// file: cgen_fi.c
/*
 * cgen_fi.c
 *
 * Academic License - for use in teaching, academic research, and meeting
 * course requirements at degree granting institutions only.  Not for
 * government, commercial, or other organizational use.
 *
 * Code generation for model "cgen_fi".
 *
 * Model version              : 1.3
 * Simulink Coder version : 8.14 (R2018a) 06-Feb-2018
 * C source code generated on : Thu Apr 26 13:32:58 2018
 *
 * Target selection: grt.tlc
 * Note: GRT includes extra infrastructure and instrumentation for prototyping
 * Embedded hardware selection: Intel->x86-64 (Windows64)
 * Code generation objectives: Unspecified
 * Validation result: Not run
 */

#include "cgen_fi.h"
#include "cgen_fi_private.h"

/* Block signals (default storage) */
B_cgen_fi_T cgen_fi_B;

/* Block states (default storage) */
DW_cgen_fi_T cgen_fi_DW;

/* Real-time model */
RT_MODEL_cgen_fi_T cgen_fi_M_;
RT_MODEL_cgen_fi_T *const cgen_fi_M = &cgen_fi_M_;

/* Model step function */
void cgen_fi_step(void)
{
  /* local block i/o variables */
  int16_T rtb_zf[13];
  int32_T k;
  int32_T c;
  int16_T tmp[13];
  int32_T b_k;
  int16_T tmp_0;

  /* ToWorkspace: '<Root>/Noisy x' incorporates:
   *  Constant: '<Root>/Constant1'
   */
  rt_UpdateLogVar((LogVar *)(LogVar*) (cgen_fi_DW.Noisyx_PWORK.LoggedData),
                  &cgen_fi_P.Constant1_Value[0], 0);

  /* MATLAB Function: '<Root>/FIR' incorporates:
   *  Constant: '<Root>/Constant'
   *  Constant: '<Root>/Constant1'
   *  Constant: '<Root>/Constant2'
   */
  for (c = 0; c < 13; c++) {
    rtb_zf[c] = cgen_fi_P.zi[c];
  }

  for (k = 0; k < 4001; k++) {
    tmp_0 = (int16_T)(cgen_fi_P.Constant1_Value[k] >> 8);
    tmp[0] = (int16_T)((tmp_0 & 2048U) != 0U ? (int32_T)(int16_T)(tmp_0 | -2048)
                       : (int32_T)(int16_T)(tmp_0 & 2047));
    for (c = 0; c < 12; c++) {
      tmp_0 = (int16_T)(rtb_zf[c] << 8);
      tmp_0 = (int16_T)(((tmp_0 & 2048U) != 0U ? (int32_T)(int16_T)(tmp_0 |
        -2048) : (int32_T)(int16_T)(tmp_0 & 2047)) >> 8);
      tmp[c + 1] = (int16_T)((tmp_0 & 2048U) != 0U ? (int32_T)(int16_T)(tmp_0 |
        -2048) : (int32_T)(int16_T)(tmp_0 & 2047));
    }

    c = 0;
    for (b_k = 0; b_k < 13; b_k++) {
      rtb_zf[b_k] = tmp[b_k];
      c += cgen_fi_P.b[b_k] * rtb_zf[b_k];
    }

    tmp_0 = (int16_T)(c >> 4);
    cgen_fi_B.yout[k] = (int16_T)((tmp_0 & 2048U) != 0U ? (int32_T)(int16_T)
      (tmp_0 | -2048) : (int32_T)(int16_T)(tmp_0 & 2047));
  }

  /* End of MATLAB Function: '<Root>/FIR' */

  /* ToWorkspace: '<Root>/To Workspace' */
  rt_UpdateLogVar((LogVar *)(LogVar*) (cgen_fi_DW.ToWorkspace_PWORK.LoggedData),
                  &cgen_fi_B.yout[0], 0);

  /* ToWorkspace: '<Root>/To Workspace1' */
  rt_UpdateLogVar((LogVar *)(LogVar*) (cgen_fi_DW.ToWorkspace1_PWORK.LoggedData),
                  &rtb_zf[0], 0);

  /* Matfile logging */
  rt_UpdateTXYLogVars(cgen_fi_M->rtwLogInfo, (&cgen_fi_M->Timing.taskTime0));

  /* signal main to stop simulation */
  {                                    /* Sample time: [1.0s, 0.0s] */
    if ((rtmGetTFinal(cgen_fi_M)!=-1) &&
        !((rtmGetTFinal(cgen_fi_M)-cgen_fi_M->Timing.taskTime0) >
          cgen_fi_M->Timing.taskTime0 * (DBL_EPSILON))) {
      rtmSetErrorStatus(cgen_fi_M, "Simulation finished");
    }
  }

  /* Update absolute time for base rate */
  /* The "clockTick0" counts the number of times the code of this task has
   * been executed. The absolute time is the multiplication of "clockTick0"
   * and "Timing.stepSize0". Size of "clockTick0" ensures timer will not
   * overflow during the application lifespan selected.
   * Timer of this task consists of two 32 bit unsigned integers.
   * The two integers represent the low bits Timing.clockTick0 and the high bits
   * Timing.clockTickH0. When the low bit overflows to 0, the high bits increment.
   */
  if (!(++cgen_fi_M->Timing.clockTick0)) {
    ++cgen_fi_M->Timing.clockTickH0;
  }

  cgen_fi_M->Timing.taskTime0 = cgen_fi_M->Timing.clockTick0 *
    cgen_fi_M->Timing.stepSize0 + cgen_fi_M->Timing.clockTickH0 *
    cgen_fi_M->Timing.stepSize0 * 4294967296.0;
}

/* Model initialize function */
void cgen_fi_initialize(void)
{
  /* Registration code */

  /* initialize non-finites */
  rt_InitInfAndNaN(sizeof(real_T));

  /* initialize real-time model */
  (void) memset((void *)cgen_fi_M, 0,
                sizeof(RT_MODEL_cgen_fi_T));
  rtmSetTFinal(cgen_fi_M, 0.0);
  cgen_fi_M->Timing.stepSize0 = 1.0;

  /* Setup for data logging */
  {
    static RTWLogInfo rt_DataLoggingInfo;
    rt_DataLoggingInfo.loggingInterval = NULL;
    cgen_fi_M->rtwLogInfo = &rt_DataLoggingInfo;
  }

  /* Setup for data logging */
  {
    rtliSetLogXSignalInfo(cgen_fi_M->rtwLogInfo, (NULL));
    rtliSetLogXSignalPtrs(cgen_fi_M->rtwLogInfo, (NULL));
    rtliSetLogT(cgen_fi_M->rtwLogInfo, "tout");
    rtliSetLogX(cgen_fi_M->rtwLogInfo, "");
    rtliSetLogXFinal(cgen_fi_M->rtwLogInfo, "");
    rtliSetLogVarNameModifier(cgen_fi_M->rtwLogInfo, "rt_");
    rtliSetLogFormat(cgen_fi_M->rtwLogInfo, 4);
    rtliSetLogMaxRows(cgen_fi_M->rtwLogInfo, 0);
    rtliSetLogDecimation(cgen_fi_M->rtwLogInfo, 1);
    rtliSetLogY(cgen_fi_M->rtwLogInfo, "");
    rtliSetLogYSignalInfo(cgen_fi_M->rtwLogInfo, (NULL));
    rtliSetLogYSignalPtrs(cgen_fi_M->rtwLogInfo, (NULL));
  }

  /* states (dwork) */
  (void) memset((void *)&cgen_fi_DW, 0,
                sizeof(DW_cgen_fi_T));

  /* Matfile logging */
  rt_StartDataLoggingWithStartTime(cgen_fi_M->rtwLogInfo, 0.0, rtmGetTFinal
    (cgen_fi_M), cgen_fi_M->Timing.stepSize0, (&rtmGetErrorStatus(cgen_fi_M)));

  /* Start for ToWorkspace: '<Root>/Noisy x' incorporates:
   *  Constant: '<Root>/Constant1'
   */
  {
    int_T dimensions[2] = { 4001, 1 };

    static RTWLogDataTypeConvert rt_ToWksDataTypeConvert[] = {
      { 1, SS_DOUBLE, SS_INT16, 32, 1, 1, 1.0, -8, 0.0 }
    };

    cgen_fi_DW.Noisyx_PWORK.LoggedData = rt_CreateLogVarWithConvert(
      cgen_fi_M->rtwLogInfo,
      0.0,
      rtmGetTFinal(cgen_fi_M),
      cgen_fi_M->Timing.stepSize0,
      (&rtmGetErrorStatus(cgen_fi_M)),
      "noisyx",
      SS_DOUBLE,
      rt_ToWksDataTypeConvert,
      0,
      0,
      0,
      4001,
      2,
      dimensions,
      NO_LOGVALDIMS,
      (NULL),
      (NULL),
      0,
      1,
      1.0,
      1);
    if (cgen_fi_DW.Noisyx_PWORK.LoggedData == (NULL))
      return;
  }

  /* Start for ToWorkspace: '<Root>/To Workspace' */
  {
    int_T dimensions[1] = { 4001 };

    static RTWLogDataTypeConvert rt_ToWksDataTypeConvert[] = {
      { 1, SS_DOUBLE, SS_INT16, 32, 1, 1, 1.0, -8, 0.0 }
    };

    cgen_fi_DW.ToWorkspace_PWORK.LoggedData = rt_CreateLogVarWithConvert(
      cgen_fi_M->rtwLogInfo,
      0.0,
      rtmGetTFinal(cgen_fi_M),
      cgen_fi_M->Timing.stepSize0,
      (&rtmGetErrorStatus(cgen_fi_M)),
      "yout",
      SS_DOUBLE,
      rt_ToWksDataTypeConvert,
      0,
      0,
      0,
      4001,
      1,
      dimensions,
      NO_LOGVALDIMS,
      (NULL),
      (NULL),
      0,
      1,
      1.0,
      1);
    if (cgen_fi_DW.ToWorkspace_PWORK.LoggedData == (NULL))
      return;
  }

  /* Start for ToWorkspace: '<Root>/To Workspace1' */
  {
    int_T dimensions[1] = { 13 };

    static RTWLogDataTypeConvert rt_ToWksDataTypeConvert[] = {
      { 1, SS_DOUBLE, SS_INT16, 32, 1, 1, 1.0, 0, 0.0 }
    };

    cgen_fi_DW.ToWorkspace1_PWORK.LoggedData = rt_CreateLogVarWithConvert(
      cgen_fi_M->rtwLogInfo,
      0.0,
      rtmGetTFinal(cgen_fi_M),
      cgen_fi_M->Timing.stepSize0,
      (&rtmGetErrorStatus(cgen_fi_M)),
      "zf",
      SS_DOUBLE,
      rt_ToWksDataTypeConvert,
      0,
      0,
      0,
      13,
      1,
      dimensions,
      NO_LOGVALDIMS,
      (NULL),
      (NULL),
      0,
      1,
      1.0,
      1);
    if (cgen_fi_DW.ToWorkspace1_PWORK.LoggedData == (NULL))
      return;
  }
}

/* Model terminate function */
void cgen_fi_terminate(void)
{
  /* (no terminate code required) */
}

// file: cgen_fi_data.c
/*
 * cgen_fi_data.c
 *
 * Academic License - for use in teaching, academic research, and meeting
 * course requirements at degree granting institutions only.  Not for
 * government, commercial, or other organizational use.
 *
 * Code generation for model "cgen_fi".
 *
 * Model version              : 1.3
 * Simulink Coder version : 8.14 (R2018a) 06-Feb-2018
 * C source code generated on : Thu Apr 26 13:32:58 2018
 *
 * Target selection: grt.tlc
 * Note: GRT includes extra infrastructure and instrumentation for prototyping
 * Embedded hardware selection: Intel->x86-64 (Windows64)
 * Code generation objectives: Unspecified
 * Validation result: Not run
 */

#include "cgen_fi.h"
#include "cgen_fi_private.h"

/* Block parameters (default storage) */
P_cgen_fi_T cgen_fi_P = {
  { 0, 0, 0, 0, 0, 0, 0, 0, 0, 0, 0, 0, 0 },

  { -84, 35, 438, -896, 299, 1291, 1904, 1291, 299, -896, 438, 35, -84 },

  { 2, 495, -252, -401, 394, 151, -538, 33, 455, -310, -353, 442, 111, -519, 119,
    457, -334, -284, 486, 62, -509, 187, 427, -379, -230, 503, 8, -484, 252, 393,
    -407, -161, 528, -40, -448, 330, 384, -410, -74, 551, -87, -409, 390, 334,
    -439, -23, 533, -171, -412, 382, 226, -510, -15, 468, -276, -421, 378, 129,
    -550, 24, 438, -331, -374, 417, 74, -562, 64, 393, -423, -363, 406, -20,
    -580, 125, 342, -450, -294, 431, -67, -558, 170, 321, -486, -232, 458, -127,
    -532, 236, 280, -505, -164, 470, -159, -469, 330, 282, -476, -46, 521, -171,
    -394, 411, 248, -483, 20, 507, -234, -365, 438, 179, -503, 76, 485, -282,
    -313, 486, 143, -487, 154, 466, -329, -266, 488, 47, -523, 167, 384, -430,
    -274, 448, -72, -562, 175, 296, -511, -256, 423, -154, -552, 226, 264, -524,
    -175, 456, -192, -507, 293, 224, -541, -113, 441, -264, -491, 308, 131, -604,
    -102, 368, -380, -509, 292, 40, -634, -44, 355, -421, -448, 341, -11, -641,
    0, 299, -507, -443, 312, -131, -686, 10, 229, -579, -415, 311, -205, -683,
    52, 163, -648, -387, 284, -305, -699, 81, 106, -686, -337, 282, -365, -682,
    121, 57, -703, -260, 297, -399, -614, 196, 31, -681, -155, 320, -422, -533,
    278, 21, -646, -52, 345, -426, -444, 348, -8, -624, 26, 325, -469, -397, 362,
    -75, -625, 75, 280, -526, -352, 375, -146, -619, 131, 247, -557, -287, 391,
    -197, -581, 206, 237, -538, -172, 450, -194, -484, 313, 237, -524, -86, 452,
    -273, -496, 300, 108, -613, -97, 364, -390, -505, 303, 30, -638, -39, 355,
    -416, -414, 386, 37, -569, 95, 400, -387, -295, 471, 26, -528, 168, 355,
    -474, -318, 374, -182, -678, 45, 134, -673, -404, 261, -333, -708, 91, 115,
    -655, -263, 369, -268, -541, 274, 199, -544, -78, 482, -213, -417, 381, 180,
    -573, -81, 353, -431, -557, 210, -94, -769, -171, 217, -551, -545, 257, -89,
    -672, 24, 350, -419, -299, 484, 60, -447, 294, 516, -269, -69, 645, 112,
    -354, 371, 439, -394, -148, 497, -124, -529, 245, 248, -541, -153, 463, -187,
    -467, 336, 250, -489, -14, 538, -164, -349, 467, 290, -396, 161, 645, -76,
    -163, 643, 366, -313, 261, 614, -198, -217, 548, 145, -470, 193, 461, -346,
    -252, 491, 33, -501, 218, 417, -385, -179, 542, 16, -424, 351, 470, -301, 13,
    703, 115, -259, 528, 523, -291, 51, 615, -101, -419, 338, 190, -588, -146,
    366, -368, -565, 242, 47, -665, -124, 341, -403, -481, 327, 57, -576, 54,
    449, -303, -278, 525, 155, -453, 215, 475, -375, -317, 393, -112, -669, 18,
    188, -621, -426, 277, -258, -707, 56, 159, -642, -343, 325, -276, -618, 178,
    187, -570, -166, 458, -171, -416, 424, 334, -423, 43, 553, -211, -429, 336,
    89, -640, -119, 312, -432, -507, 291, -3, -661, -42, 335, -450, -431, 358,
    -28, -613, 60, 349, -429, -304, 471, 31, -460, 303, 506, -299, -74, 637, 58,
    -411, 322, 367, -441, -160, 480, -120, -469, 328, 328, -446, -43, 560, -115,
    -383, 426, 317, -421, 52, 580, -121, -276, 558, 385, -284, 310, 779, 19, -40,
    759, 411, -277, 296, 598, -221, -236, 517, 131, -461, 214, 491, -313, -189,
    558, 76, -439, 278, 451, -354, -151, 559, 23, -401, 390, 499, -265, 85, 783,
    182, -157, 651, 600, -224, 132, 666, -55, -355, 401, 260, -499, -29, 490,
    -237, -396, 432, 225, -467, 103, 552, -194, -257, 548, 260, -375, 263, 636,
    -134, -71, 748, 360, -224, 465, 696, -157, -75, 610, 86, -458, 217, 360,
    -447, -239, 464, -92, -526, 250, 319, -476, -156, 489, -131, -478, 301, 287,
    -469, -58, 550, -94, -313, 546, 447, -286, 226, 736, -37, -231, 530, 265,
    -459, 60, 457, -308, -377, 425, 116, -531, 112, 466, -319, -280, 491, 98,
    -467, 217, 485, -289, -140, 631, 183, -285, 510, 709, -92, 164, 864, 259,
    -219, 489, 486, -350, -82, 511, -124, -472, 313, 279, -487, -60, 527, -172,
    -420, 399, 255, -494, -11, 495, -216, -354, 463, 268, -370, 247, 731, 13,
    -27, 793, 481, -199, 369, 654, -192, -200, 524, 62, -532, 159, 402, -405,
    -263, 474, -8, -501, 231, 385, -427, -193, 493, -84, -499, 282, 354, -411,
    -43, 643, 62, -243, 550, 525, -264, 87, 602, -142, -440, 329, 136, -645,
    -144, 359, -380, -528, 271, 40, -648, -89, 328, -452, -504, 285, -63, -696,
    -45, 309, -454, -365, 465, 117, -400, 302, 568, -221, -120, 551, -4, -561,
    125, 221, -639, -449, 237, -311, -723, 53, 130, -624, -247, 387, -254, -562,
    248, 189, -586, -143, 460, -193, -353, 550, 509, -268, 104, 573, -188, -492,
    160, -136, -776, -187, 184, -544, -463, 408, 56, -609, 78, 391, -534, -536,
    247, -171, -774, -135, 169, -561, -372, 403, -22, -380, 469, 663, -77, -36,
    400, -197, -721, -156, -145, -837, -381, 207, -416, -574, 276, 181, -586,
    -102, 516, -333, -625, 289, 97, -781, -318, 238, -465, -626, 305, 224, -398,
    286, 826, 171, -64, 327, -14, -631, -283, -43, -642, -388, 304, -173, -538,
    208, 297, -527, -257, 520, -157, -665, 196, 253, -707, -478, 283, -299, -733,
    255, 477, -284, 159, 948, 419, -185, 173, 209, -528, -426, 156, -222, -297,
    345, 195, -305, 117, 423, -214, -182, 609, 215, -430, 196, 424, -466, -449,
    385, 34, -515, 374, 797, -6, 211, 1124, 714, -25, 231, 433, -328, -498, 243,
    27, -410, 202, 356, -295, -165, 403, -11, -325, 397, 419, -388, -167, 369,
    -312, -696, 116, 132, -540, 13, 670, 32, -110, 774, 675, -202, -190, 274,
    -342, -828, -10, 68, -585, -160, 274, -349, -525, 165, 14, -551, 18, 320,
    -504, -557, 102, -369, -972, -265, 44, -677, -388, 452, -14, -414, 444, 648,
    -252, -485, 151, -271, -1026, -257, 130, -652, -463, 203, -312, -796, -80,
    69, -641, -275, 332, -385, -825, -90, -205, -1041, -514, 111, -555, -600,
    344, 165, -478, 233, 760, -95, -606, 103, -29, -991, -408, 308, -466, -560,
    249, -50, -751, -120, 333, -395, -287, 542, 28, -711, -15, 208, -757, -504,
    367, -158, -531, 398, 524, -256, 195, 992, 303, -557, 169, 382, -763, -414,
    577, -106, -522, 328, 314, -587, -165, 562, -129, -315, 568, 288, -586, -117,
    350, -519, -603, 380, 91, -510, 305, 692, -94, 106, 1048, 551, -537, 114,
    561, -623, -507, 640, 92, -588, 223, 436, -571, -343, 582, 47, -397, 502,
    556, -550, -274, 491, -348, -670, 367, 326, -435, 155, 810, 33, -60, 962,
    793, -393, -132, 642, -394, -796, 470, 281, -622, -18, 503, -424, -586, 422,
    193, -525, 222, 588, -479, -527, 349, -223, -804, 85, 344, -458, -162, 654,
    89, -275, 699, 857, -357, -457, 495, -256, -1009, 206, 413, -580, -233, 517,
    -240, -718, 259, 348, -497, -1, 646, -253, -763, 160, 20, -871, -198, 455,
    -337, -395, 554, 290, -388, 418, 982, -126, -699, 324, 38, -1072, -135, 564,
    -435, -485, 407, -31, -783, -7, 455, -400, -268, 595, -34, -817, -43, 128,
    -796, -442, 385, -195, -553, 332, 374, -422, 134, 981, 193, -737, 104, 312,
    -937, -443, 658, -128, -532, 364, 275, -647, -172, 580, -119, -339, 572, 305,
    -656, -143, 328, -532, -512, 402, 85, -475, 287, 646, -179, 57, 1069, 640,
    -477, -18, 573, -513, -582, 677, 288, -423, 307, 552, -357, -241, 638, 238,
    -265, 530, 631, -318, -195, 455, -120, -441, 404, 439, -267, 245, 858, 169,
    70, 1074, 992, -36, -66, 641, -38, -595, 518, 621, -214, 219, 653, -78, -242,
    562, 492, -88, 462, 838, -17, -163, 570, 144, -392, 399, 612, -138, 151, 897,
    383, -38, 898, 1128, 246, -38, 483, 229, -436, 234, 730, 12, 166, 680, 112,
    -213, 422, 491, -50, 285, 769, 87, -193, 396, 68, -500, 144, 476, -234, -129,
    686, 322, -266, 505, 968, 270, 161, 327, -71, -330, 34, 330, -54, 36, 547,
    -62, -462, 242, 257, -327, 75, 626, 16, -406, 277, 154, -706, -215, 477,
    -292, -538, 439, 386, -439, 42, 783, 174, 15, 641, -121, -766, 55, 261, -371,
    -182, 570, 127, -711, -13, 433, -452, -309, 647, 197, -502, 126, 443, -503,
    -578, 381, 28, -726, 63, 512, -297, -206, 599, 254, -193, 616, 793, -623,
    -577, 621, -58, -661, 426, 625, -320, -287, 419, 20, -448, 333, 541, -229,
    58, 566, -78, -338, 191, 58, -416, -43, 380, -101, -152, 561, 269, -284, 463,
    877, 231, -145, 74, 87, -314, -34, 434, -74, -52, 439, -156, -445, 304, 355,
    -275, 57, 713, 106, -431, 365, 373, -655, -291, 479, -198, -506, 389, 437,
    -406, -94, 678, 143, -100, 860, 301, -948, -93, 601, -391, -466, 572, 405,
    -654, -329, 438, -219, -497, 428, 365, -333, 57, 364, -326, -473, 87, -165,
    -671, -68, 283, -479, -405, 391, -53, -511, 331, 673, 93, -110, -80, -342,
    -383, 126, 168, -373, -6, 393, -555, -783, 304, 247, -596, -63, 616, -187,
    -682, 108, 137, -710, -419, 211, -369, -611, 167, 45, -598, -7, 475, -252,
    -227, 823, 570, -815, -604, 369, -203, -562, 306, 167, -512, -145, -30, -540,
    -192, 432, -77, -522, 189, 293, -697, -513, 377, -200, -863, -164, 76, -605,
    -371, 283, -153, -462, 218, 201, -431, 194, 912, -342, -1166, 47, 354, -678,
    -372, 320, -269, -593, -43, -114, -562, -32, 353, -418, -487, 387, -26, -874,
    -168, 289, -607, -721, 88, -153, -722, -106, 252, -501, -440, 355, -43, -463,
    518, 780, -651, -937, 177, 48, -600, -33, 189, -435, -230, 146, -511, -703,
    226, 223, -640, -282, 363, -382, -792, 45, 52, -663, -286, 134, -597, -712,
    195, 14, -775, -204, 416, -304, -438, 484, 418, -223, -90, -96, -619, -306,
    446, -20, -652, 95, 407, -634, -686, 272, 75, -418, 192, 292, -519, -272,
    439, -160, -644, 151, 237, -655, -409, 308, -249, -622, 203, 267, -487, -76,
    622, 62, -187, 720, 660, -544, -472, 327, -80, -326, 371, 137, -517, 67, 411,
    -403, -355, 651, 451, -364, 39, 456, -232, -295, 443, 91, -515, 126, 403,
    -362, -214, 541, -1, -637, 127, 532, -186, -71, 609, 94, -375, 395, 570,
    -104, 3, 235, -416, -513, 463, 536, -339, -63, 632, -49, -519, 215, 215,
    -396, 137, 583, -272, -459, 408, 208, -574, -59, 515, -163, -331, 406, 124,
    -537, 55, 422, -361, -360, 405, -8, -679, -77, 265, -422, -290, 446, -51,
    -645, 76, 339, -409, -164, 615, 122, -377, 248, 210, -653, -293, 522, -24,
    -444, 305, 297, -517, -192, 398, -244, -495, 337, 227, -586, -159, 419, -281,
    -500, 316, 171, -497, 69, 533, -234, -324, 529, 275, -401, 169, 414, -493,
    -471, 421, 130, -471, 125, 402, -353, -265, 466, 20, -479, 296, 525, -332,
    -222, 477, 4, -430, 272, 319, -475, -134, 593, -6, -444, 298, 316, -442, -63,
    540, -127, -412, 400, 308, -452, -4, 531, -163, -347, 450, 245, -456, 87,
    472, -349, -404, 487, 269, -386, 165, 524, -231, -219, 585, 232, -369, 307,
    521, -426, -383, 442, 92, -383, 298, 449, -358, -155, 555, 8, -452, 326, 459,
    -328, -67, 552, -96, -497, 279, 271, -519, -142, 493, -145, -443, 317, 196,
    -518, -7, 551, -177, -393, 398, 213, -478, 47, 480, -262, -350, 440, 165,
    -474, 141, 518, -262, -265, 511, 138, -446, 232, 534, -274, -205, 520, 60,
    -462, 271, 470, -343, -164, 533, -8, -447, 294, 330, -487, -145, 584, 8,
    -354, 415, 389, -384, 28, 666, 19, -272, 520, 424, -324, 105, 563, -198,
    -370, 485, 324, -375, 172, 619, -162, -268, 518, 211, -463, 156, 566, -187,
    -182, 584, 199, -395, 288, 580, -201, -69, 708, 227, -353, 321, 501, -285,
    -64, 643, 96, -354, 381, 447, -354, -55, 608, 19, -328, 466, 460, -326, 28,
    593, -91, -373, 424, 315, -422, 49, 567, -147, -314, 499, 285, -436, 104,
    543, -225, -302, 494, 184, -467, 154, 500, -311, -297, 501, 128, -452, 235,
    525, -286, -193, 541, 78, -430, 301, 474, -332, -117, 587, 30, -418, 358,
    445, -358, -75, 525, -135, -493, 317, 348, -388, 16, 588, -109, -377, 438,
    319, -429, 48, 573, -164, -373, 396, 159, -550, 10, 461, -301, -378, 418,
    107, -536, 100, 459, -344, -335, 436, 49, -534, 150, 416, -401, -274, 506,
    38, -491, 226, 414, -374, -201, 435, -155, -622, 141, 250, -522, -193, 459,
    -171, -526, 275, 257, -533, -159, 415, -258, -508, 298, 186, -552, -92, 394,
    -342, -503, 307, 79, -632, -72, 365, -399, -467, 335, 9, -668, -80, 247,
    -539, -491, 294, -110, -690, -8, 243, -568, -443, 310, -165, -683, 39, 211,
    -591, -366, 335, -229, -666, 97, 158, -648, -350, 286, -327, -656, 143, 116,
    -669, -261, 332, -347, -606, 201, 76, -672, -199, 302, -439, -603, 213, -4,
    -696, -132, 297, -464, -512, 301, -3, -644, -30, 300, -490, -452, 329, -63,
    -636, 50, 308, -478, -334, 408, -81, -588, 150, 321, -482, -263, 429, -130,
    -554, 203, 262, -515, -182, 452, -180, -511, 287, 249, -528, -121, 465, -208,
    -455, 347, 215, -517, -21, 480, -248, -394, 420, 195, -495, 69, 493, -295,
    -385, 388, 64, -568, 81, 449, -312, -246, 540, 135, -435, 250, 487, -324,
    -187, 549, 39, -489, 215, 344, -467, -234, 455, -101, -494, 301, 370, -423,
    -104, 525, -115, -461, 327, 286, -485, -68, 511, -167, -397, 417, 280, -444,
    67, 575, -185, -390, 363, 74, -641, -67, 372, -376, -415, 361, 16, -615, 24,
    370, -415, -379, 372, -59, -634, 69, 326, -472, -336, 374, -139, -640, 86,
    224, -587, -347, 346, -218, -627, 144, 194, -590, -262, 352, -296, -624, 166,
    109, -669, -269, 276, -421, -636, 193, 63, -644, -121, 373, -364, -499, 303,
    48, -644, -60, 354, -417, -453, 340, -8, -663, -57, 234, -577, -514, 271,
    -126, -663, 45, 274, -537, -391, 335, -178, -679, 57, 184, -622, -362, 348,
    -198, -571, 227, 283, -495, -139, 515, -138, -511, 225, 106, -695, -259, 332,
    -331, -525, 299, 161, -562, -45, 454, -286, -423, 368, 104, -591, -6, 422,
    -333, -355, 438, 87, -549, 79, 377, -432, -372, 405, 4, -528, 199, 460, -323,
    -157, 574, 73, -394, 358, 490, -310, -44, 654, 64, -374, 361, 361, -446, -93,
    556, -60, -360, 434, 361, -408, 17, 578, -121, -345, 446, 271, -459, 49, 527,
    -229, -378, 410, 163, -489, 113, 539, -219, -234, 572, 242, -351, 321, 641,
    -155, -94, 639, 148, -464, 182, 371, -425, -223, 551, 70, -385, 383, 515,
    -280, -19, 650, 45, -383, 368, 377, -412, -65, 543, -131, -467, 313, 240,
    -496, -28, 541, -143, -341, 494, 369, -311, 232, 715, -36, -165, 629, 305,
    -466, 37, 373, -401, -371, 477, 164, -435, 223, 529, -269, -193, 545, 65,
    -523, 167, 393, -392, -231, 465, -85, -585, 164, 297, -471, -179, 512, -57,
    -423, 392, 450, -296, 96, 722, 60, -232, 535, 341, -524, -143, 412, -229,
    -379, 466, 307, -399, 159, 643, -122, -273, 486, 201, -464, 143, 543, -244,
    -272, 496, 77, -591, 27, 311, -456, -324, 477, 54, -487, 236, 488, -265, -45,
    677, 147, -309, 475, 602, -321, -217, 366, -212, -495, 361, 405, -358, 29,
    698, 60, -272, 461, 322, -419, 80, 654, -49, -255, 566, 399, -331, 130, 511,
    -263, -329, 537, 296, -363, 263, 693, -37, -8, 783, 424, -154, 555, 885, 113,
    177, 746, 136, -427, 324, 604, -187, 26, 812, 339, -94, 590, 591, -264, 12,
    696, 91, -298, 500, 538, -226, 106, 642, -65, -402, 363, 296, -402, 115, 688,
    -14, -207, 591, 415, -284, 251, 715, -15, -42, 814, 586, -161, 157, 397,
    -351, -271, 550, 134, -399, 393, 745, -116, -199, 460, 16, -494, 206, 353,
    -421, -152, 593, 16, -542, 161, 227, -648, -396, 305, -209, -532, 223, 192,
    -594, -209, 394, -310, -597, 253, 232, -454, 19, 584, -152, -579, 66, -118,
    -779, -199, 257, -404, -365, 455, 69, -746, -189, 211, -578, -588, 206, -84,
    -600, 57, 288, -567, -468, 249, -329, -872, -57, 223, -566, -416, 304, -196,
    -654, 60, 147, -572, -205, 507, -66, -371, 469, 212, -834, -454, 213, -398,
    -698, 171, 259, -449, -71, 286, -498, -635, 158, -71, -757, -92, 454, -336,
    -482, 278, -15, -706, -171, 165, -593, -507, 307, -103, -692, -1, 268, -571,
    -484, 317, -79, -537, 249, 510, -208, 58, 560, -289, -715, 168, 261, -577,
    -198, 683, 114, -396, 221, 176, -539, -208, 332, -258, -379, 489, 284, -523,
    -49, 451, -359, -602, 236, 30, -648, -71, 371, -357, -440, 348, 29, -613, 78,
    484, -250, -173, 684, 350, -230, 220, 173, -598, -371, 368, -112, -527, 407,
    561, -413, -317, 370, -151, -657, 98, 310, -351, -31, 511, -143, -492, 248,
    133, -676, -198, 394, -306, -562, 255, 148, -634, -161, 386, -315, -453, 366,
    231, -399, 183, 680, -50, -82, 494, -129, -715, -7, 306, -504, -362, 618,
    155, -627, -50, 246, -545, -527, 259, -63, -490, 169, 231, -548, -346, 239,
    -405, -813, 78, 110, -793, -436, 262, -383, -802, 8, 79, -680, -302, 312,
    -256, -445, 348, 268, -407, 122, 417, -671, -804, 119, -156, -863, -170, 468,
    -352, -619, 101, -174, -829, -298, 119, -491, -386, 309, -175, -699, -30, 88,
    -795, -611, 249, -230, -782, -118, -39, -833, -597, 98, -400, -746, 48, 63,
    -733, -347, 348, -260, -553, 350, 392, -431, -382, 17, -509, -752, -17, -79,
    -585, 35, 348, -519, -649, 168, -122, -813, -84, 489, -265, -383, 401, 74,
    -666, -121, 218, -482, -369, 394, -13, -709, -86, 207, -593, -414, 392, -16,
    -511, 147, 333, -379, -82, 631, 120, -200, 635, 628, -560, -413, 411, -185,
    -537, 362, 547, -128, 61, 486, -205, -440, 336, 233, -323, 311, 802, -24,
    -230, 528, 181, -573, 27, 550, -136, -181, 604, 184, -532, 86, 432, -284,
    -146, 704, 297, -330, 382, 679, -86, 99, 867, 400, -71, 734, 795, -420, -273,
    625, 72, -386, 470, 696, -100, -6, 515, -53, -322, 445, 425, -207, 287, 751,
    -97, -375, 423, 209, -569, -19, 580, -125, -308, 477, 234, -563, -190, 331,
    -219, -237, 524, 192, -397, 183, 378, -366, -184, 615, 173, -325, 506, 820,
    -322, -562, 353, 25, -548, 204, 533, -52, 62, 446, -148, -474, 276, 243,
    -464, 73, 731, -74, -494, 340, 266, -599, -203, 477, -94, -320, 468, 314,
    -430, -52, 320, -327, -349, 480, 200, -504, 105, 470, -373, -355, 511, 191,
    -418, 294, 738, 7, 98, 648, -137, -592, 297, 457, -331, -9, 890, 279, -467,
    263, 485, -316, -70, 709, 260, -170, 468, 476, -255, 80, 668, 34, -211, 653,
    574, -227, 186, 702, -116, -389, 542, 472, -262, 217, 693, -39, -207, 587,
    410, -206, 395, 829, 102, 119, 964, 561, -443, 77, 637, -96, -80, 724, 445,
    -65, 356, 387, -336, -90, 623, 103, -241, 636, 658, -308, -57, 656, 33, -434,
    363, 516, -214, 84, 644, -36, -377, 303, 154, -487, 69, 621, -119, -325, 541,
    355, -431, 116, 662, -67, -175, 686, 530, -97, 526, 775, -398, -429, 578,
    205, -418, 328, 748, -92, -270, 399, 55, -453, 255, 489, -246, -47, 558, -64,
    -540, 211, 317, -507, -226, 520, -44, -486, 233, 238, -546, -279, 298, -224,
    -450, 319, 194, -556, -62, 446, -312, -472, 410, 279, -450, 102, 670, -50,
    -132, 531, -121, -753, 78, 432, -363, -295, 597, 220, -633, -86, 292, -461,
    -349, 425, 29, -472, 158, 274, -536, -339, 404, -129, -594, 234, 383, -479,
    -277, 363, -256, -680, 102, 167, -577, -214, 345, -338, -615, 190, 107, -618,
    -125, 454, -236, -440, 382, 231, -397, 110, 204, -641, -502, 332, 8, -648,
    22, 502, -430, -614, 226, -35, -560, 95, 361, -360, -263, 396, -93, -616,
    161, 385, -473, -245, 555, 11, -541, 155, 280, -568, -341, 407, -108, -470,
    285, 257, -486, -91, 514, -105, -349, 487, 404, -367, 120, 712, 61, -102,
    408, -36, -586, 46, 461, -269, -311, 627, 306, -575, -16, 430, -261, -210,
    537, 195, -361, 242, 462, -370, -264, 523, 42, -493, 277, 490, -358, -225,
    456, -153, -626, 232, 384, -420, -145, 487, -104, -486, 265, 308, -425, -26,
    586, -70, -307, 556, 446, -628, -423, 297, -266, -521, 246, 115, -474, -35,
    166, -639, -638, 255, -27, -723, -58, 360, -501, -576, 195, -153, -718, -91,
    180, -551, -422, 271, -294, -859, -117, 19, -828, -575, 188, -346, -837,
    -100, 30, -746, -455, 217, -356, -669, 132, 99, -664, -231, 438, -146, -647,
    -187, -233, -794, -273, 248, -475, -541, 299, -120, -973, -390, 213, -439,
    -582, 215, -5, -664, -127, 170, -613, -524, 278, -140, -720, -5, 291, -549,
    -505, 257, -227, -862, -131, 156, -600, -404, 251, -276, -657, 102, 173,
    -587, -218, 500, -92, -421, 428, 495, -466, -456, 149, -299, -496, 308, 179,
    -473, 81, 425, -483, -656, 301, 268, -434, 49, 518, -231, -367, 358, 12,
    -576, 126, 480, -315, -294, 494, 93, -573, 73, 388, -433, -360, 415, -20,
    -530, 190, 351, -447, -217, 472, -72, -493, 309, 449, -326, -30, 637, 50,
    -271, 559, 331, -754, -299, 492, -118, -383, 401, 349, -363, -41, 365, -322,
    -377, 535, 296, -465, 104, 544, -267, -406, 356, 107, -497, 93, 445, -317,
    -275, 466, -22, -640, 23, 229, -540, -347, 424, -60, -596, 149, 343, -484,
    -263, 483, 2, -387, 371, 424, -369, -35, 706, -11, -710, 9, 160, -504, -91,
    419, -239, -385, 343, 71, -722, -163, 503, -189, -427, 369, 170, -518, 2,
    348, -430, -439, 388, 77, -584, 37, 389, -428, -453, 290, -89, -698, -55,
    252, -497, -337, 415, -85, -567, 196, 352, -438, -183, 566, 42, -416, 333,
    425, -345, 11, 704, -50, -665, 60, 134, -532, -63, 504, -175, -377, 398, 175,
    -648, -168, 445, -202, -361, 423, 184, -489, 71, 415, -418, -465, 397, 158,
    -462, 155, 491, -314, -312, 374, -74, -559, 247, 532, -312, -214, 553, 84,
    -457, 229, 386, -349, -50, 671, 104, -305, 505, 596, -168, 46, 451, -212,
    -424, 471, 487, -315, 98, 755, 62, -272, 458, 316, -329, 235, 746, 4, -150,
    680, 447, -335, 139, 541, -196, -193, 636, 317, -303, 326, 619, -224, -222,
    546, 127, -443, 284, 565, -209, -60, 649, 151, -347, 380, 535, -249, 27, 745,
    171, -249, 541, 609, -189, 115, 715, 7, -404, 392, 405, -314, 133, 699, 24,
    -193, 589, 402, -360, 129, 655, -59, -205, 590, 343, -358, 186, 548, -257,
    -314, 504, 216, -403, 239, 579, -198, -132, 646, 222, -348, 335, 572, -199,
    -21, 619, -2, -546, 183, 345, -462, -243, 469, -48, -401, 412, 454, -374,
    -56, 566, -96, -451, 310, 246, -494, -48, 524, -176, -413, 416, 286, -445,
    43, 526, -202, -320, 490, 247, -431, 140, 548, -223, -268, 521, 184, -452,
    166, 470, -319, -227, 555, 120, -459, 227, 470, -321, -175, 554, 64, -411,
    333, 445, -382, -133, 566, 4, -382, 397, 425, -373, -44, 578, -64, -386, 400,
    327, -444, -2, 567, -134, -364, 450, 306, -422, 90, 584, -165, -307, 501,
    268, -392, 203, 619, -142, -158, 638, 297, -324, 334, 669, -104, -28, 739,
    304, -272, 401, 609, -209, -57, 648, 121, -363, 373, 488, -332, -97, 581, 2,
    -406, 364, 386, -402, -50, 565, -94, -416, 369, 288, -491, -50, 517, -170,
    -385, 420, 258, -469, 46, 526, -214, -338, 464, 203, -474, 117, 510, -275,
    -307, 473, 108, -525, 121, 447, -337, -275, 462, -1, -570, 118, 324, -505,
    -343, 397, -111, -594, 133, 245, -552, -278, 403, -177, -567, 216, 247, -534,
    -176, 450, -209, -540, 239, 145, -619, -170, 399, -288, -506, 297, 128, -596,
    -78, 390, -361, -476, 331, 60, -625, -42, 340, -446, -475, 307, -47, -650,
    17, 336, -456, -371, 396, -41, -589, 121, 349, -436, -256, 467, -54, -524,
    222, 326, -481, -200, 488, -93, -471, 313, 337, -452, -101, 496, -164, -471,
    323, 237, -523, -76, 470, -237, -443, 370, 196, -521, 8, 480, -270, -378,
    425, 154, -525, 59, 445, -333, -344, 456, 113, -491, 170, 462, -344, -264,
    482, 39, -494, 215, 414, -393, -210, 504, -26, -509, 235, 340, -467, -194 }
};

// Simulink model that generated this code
simulink model "cgen_fi"  (R2018a)
settings: Solver=FixedStepDiscrete  StartTime=0.0  StopTime=0  RelTol=1e-3
values from neighbouring files (symbols this model uses):
  b = fidemo.fi_fir_coefficients    [setFIRInputs.m]
  noise = sin(2*pi*2140*(0:n-1)'./Fs)    [setFIRInputs.m]
  x = x + noise    [setFIRInputs.m]
  zi = zeros(length(b),1)    [setFIRInputs.m]

== system cgen_fi ==
  Constant : Constant  Value=b  VectorParams1D=off  OutDataTypeStr=fixdt(1,12,2^-12,0)
  Constant1 : Constant  Value=x+noise  VectorParams1D=off  OutDataTypeStr=fixdt(1,12,2^-8,0)  SampleTime=1
  Constant2 : Constant  Value=zi  VectorParams1D=off  OutDataTypeStr=fixdt(1,12,2^0,0)
  FIR : MATLAB Function  TreatAsAtomicUnit=on
  Noisy x : ToWorkspace  VariableName=noisyx  SampleTime=-1
  To Workspace : ToWorkspace  VariableName=yout  SampleTime=-1
  To Workspace1 : ToWorkspace  VariableName=zf  SampleTime=-1
  wires:
  Constant/1 -> FIR/1(b)
  Constant2/1 -> FIR/3(zi)
  Constant1/1 -> Noisy x/1, FIR/2(x)
  FIR/1(yout) -> To Workspace/1
  FIR/2(zf) -> To Workspace1/1

== matlab function cgen_fi/FIR ==
  settings: fimath=|
      | fimath('RoundingMethod','Floor','OverflowAction','Wrap',...
      |     'ProductMode','KeepLSB','ProductWordLength',32,...
      |     'SumMode','KeepLSB','SumWordLength',32)
function [yout,zf] = dffirdemo(b, x, zi) %#codegen
%codegen_fi doc model example
%Initialize the output signal yout and the final conditions zf
Ty = numerictype(1,12,8);
yout = fi(zeros(size(x)),'numerictype',Ty);
zf = zi;

% FIR filter code
for k=1:length(x);
  % Update the states: z = [x(k);z(1:end-1)]  
  zf(:) = [x(k);zf(1:end-1)];
  % Form the output: y(k) = b*z
  yout(k) = b*zf;
end

% Plot the outputs only in simulation.
% This does not generate C code.
figure;
subplot(211);plot(x); title('Noisy Signal');grid;
subplot(212);plot(yout); title('Filtered Signal');grid;
